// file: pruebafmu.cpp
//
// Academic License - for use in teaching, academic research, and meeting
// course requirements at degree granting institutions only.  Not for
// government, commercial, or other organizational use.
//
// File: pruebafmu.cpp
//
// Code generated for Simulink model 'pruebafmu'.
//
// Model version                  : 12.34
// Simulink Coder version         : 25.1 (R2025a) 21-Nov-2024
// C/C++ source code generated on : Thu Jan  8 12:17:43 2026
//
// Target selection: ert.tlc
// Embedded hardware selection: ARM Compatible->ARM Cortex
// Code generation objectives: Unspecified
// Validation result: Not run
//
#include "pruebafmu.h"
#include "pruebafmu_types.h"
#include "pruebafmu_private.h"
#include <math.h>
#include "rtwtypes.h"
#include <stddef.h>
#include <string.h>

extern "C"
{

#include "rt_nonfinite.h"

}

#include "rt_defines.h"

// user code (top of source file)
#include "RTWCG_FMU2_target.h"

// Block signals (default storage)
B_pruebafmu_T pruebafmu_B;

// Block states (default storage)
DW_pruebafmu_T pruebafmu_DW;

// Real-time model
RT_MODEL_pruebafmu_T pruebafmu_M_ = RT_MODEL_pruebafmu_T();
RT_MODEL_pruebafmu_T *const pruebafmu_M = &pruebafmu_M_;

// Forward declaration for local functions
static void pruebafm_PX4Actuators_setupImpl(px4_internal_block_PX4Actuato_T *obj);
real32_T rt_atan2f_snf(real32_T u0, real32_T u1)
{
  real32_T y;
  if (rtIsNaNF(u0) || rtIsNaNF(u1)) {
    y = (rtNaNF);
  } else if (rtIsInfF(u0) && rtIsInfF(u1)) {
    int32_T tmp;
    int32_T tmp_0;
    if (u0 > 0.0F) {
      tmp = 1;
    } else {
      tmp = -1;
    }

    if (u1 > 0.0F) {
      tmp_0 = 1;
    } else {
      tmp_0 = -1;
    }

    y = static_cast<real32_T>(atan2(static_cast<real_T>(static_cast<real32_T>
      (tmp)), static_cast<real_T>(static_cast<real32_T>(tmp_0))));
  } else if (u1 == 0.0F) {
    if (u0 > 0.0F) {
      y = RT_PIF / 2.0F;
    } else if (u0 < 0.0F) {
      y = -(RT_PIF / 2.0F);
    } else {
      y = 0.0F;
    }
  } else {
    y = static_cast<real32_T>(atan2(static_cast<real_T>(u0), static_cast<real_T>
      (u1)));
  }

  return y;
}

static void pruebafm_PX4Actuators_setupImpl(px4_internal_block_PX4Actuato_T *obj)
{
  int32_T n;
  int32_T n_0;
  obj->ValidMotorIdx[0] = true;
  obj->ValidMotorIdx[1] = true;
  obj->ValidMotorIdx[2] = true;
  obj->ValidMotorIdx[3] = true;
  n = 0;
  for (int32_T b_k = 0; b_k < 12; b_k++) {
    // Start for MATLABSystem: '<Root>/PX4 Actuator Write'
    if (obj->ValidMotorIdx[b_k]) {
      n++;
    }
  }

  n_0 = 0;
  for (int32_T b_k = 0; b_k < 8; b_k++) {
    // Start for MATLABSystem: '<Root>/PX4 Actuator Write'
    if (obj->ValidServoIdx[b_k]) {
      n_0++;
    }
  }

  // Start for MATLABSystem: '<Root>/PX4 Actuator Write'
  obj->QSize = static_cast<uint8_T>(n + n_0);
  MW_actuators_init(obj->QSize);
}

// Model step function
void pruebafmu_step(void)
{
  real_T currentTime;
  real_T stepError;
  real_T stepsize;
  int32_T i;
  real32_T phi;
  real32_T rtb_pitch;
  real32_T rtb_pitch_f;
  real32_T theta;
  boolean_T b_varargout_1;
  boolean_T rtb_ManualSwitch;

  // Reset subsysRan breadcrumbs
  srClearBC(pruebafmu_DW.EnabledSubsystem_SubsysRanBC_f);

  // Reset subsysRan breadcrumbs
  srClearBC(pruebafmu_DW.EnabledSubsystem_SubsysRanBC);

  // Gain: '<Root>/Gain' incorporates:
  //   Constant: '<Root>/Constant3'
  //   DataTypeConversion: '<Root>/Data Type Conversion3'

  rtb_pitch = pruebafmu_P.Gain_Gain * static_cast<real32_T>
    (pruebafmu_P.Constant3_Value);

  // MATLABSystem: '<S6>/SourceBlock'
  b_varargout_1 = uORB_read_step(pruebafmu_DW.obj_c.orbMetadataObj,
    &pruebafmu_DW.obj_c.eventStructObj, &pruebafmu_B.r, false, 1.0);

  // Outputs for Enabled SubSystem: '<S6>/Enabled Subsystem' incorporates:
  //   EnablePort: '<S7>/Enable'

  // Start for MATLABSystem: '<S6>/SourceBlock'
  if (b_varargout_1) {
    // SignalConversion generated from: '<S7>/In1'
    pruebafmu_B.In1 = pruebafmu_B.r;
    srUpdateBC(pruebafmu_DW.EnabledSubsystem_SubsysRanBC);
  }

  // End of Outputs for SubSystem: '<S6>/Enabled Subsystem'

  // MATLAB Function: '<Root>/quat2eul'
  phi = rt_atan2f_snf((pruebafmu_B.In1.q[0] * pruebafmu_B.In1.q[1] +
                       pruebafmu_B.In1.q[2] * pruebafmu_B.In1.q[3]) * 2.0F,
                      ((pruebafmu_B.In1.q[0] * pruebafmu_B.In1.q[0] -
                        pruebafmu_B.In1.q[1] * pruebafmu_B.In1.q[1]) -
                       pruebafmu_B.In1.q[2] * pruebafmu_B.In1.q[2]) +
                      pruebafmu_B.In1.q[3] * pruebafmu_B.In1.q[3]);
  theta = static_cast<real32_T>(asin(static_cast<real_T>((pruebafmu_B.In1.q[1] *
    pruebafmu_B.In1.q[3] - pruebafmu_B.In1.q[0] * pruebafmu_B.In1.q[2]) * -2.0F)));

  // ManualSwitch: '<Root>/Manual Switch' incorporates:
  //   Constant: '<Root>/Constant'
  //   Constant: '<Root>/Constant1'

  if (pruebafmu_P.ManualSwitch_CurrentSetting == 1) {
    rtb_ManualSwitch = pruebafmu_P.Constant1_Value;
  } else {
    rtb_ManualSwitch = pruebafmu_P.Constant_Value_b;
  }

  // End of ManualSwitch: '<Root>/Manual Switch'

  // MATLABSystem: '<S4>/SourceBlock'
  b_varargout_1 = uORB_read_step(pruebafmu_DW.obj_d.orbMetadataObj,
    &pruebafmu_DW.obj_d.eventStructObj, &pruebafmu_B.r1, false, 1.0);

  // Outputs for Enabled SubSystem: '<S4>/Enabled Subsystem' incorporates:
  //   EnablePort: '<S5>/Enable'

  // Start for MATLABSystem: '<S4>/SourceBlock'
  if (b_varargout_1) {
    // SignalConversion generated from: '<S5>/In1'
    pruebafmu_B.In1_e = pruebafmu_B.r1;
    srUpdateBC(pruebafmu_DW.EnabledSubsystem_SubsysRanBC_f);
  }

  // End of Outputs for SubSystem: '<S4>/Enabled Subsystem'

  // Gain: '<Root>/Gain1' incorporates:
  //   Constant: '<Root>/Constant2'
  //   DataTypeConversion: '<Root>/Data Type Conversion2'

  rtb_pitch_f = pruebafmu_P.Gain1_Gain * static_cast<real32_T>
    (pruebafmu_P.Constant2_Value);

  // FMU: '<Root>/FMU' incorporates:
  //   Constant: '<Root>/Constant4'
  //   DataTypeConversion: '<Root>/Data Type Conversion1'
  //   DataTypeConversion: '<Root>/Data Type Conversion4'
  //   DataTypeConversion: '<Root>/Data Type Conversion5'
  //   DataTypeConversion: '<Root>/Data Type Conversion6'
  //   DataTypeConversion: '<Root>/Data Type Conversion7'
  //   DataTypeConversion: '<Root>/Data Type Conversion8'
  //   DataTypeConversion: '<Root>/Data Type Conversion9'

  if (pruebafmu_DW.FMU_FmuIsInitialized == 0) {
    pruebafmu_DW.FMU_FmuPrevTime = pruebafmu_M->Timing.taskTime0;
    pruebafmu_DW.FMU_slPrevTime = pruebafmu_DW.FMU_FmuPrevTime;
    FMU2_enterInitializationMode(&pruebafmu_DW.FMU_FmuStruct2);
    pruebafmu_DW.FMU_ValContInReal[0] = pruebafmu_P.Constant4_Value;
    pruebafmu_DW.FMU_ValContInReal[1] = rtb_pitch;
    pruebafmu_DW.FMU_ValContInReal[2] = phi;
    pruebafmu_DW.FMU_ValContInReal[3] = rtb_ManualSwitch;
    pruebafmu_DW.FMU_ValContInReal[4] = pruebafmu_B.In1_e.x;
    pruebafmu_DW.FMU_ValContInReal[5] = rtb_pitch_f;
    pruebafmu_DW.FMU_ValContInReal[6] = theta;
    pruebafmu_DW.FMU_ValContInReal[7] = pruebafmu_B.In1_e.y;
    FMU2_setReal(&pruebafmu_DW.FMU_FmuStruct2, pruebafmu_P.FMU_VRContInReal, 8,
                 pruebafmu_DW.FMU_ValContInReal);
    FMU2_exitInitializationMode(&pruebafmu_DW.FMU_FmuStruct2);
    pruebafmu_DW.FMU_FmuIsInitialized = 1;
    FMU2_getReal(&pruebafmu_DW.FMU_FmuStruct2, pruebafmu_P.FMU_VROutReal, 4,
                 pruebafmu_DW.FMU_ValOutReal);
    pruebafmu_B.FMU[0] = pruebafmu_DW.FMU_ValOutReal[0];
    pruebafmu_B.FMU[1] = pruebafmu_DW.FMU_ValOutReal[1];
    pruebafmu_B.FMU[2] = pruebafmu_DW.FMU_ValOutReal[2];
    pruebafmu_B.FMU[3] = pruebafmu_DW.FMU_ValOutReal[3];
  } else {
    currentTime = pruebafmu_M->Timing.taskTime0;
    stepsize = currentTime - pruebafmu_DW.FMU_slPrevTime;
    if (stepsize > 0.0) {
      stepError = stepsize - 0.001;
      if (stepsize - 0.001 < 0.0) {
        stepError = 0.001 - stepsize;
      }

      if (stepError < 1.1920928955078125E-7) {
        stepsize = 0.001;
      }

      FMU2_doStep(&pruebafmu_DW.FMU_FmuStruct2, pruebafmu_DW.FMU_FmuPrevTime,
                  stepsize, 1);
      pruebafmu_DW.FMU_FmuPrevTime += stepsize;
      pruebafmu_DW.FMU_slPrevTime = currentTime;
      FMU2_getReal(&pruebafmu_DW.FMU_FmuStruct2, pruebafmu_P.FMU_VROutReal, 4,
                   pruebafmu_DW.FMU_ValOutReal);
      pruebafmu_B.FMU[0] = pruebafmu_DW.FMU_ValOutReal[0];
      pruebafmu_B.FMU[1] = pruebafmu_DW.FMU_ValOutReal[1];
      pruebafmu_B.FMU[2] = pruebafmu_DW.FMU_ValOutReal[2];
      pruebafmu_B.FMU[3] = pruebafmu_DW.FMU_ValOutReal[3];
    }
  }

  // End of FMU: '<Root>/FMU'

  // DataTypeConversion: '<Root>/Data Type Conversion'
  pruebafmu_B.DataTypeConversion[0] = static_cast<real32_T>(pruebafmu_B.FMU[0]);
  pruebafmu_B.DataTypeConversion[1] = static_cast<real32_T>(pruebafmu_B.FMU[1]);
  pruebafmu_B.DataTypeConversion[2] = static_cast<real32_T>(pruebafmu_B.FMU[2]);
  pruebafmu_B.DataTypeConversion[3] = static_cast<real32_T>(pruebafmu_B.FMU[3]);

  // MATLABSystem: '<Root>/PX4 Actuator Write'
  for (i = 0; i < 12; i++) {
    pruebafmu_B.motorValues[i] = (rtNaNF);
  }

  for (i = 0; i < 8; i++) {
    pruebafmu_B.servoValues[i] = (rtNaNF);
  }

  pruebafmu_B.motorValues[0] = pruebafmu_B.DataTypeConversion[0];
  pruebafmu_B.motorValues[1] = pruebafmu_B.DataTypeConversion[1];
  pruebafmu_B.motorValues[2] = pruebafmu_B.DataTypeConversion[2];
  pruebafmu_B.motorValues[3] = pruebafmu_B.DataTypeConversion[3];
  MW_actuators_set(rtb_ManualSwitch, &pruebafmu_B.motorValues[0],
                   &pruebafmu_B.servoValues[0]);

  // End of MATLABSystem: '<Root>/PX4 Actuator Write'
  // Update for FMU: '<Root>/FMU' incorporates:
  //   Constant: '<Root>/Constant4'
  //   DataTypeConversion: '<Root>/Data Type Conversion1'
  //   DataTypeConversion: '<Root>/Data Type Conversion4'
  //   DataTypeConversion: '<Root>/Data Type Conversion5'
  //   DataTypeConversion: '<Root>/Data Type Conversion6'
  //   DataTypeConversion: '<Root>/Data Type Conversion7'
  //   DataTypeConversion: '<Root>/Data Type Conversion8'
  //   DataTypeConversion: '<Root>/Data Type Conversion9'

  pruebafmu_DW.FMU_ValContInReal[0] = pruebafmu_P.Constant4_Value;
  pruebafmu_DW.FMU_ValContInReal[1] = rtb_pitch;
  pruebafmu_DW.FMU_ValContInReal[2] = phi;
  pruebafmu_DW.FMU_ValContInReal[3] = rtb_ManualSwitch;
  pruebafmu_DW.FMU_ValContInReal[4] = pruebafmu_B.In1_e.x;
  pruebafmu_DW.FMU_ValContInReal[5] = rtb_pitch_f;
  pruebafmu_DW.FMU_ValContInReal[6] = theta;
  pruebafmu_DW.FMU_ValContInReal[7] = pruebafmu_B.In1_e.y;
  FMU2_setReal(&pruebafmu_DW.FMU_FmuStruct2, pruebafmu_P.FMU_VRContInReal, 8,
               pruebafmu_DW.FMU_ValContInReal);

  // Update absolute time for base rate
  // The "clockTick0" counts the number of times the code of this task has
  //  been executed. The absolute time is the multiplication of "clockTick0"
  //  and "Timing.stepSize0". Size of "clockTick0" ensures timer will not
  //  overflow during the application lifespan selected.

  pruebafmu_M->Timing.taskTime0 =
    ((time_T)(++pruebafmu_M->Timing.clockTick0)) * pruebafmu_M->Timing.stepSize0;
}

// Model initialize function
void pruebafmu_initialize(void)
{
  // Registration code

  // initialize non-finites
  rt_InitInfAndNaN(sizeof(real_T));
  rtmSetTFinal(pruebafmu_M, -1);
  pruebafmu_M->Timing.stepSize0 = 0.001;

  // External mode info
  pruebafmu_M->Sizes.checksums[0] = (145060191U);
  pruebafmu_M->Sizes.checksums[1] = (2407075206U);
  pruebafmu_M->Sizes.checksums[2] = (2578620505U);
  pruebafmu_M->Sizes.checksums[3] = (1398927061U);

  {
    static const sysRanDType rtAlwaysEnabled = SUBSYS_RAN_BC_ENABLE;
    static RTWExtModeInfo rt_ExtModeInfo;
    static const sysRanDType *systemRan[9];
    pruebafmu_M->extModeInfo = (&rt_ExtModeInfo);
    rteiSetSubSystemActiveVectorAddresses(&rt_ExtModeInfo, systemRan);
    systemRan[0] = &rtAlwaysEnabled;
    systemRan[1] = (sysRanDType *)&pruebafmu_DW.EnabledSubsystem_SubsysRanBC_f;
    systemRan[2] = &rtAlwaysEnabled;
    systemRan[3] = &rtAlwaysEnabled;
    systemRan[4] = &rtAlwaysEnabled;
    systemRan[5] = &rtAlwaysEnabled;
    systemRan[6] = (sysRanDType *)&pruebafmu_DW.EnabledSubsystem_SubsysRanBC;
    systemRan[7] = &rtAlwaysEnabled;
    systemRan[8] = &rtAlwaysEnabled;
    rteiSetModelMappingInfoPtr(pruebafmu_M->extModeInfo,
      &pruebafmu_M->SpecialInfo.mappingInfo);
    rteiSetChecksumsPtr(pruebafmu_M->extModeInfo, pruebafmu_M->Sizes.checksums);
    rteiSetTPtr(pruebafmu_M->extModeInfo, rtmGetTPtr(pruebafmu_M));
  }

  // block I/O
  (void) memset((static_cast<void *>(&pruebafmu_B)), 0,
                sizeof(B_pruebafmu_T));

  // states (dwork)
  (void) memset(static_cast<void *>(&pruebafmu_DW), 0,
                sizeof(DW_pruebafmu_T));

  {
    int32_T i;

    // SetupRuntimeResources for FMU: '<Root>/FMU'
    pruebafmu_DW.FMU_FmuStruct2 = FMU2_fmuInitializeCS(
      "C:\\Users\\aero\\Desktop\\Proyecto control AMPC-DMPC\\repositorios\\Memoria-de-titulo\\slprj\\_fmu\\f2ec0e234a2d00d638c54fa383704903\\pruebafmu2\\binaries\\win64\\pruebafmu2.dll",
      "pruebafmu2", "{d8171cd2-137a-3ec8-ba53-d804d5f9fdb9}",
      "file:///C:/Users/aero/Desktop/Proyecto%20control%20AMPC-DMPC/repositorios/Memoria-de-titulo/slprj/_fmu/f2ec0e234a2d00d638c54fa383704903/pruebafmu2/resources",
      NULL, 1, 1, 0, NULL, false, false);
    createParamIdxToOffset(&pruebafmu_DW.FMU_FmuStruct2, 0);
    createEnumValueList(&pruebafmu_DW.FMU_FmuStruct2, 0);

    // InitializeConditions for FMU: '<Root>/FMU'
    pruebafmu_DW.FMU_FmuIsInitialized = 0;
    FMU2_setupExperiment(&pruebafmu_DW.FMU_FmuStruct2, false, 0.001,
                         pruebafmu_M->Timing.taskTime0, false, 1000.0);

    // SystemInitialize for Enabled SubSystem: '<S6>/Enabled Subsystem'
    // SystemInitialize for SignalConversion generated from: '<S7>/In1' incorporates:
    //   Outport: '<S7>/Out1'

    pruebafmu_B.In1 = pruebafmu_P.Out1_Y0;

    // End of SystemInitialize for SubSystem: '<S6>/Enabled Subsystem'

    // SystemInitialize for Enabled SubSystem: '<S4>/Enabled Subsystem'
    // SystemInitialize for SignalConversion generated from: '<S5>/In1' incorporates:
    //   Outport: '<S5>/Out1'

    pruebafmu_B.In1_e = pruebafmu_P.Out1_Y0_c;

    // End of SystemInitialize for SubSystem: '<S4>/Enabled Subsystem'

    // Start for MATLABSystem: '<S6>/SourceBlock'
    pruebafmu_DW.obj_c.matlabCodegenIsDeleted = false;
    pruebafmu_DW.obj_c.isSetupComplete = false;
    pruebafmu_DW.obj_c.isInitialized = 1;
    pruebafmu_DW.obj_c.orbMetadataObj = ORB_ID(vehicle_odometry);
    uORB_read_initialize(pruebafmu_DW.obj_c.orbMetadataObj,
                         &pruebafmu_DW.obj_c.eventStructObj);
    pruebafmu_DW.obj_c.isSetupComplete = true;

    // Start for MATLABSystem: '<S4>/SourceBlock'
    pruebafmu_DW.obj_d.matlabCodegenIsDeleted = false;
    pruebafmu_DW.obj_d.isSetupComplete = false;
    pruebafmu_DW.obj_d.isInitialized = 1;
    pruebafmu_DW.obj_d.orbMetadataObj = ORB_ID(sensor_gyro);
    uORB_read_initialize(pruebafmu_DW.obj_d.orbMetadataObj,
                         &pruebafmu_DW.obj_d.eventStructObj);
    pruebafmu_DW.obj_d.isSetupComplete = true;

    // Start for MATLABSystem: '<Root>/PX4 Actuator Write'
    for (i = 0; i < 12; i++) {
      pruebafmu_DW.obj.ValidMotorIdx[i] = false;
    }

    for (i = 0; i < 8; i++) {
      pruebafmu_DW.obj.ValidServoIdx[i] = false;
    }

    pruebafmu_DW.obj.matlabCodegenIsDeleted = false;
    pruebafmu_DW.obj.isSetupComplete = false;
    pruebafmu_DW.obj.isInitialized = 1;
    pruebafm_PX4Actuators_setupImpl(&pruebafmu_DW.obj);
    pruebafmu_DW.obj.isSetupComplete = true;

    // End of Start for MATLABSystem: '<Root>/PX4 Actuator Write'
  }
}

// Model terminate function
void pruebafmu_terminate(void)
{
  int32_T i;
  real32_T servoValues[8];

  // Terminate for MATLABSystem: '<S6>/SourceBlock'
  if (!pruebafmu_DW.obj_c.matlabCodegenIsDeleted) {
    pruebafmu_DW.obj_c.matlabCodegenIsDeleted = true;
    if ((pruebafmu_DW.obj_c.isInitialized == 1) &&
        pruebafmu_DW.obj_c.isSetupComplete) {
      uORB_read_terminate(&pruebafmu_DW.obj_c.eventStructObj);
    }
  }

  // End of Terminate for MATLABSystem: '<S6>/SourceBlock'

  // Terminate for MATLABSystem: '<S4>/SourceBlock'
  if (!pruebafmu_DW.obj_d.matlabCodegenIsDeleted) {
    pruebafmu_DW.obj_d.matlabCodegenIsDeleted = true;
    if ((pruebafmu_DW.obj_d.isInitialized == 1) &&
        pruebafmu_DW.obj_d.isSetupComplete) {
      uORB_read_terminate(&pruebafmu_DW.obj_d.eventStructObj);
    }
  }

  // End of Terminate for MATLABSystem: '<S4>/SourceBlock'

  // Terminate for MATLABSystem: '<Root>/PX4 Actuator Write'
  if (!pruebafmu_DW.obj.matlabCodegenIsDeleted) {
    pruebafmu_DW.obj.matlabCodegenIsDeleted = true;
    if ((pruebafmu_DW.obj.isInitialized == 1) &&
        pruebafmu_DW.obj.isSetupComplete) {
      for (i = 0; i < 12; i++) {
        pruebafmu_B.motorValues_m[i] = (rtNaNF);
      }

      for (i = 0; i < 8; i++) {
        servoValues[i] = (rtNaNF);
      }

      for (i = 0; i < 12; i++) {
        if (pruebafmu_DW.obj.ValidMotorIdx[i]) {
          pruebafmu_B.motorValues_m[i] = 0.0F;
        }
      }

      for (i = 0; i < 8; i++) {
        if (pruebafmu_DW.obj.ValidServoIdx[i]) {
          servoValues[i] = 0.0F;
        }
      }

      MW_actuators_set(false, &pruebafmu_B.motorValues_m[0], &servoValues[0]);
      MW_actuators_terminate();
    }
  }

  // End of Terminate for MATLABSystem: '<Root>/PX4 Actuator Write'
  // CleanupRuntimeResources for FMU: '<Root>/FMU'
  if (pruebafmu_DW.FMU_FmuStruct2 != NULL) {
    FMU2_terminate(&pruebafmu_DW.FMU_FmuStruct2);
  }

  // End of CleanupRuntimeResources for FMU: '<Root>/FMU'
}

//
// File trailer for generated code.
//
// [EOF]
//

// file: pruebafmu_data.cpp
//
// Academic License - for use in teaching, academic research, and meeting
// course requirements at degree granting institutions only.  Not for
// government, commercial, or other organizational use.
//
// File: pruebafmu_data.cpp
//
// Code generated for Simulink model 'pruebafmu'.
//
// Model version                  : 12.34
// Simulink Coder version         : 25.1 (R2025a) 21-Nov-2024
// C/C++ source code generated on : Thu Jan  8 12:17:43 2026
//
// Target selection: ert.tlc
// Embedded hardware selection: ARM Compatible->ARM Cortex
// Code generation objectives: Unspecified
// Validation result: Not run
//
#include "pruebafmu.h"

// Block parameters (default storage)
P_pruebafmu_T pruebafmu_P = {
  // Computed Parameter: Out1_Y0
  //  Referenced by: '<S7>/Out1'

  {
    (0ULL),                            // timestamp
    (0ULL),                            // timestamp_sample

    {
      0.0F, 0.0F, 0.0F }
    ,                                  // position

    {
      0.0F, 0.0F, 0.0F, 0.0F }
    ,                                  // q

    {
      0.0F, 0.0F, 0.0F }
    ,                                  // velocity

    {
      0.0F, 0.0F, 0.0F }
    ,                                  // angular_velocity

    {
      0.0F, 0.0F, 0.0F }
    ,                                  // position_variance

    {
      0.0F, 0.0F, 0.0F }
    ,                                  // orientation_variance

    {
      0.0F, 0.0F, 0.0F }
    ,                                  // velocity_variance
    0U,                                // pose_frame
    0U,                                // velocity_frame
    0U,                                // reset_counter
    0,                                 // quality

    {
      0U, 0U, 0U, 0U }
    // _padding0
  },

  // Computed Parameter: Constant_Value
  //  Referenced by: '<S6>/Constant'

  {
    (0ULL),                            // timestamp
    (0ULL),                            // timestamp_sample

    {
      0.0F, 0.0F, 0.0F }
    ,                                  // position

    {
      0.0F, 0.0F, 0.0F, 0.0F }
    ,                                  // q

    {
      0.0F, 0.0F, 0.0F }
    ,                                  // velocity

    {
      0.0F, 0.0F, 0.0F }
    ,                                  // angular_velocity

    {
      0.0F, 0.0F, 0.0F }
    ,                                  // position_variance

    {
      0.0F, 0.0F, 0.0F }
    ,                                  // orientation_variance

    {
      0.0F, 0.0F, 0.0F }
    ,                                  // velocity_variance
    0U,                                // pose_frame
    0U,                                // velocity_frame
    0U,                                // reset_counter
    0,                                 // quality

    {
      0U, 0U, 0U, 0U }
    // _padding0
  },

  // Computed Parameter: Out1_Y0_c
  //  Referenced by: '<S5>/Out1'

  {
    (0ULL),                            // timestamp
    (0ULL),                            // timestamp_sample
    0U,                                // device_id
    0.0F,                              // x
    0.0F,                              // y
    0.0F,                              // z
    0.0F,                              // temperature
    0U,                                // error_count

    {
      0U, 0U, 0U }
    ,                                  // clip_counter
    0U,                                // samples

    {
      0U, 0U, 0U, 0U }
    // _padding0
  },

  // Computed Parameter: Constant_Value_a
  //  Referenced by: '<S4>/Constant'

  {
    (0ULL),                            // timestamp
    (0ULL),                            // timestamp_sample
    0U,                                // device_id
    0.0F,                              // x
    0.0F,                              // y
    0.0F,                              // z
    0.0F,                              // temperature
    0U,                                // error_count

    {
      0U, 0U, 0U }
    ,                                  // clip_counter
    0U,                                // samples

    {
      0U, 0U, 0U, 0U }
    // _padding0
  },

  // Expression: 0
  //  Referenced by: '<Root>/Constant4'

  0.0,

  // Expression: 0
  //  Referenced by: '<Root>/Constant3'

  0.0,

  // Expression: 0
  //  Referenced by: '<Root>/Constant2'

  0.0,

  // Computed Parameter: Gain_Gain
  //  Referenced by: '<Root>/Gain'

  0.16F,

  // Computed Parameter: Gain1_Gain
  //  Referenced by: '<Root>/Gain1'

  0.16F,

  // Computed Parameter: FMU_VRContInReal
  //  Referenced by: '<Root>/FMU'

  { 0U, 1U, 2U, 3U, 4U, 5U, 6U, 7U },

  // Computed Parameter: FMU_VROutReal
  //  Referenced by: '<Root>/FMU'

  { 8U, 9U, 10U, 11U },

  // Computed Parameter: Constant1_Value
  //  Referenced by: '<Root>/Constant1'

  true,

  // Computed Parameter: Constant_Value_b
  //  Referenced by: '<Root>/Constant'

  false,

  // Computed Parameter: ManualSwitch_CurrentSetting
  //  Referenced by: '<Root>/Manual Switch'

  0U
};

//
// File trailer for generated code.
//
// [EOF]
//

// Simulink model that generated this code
simulink model "pruebafmu"  (R2025a)
settings: Solver=FixedStepAuto  StartTime=0.0  StopTime=inf  FixedStep=0.001  RelTol=1e-3  EnableMultiTasking=on
libraries: px4Sensorslib x2, px4Peripheralslib x1

== system pruebafmu ==
  Constant : Constant  Value=0  OutDataTypeStr=boolean
  Constant1 : Constant  OutDataTypeStr=boolean
  Constant2 : Constant  Value=0
  Constant3 : Constant  Value=0
  Constant4 : Constant  Value=0
  Data Type Conversion : DataTypeConversion  OutDataTypeStr=single  SaturateOnIntegerOverflow=off  RndMeth=Floor
  Data Type Conversion{1,4..9} (7 alike) : DataTypeConversion  OutDataTypeStr=double  SaturateOnIntegerOverflow=off  RndMeth=Floor
  Data Type Conversion2 : DataTypeConversion  OutDataTypeStr=single  SaturateOnIntegerOverflow=off  RndMeth=Floor
  Data Type Conversion3 : DataTypeConversion  OutDataTypeStr=single  SaturateOnIntegerOverflow=off  RndMeth=Floor
  Demux : Demux
  FMU : FMU  FMUName=pruebafmu2.fmu  FMUMode=CoSimulation  FMUCreateBusObject=off  FMUInitializeEnumObject=off
  Gain : Gain  Gain=0.16
  Gain1 : Gain  Gain=0.16
  Gyroscope : px4Sensorslib/Gyroscope  uorbTimeStamp=off  BlockingMode=off  BlockTimeout=1e-3  sampleTime=0.001
  Manual Switch : ManualSwitch  CurrentSetting=0
  PX4 Actuator Write : px4Peripheralslib/PX4 Actuator Write  Motor1Enable=on  Motor2Enable=on  Motor3Enable=on  Motor4Enable=on  Motor5Enable=off  Motor6Enable=off  Motor7Enable=off  Motor8Enable=off  Motor9Enable=off  Motor10Enable=off  Motor11Enable=off  Motor12Enable=off  IsMotorArray=off  Servo1Enable=off  Servo2Enable=off  Servo3Enable=off  Servo4Enable=off  Servo5Enable=off  Servo6Enable=off  Servo7Enable=off  Servo8Enable=off  IsServoArray=off
  Scope1 : Scope
  Slider : SliderBlock  ScaleMax=0.5
  Terminator{,1..2,6} (4 alike) : Terminator
  Vehicle Attitude : px4Sensorslib/Vehicle Attitude  rollRate=off  pitchRate=off  yawRate=off  quaternion=on  uorbTimeStamp=off  BlockingMode=off  BlockTimeout=0.001  sampleTime=0.001
  quat2eul : MATLAB Function  TreatAsAtomicUnit=on
  wires:
  Manual Switch/1 -> Data Type Conversion1/1, PX4 Actuator Write/1
  Vehicle Attitude/1 -> Terminator/1
  Gyroscope/1 -> Terminator1/1
  Gain/1 -> Data Type Conversion4/1  "roll"
  Data Type Conversion/1 -> Scope1/1, Demux/1
  Demux/1 -> PX4 Actuator Write/2
  Demux/2 -> PX4 Actuator Write/3
  Demux/3 -> PX4 Actuator Write/4
  Demux/4 -> PX4 Actuator Write/5
  Constant/1 -> Manual Switch/2
  Constant1/1 -> Manual Switch/1
  Gyroscope/2 -> Data Type Conversion6/1  "roll rate"
  Gyroscope/4 -> Terminator6/1
  Gyroscope/3 -> Data Type Conversion7/1
  Gain1/1 -> Data Type Conversion5/1  "pitch"
  Data Type Conversion3/1 -> Gain/1
  Data Type Conversion2/1 -> Gain1/1
  Constant2/1 -> Data Type Conversion2/1
  Constant3/1 -> Data Type Conversion3/1
  Vehicle Attitude/2 -> quat2eul/1(q)
  quat2eul/2(theta) -> Data Type Conversion8/1
  quat2eul/1(phi) -> Data Type Conversion9/1  "phi"
  quat2eul/3(psi) -> Terminator2/1
  Constant4/1 -> FMU/1
  FMU/1 -> Data Type Conversion/1
  Data Type Conversion1/1 -> FMU/4
  Data Type Conversion4/1 -> FMU/2
  Data Type Conversion5/1 -> FMU/6
  Data Type Conversion6/1 -> FMU/5
  Data Type Conversion7/1 -> FMU/8
  Data Type Conversion8/1 -> FMU/7
  Data Type Conversion9/1 -> FMU/3

== matlab function pruebafmu/quat2eul ==
function [phi,theta,psi] = quat2eul(q)

% Quaternion conversion to Euler angles based on the PX4 Firmware v1.10.2
% release.

phi = atan2(2*(q(1)*q(2) + q(3)* q(4)), q(1)^2 - q(2)^2 - q(3)^2 + q(4)^2);
theta = asin(-2*(q(2)*q(4) - q(1)*q(3)));
psi = atan2(2*(q(2)*q(3) + q(1)* q(4)), q(1)^2 + q(2)^2 - q(3)^2 - q(4)^2);
end
